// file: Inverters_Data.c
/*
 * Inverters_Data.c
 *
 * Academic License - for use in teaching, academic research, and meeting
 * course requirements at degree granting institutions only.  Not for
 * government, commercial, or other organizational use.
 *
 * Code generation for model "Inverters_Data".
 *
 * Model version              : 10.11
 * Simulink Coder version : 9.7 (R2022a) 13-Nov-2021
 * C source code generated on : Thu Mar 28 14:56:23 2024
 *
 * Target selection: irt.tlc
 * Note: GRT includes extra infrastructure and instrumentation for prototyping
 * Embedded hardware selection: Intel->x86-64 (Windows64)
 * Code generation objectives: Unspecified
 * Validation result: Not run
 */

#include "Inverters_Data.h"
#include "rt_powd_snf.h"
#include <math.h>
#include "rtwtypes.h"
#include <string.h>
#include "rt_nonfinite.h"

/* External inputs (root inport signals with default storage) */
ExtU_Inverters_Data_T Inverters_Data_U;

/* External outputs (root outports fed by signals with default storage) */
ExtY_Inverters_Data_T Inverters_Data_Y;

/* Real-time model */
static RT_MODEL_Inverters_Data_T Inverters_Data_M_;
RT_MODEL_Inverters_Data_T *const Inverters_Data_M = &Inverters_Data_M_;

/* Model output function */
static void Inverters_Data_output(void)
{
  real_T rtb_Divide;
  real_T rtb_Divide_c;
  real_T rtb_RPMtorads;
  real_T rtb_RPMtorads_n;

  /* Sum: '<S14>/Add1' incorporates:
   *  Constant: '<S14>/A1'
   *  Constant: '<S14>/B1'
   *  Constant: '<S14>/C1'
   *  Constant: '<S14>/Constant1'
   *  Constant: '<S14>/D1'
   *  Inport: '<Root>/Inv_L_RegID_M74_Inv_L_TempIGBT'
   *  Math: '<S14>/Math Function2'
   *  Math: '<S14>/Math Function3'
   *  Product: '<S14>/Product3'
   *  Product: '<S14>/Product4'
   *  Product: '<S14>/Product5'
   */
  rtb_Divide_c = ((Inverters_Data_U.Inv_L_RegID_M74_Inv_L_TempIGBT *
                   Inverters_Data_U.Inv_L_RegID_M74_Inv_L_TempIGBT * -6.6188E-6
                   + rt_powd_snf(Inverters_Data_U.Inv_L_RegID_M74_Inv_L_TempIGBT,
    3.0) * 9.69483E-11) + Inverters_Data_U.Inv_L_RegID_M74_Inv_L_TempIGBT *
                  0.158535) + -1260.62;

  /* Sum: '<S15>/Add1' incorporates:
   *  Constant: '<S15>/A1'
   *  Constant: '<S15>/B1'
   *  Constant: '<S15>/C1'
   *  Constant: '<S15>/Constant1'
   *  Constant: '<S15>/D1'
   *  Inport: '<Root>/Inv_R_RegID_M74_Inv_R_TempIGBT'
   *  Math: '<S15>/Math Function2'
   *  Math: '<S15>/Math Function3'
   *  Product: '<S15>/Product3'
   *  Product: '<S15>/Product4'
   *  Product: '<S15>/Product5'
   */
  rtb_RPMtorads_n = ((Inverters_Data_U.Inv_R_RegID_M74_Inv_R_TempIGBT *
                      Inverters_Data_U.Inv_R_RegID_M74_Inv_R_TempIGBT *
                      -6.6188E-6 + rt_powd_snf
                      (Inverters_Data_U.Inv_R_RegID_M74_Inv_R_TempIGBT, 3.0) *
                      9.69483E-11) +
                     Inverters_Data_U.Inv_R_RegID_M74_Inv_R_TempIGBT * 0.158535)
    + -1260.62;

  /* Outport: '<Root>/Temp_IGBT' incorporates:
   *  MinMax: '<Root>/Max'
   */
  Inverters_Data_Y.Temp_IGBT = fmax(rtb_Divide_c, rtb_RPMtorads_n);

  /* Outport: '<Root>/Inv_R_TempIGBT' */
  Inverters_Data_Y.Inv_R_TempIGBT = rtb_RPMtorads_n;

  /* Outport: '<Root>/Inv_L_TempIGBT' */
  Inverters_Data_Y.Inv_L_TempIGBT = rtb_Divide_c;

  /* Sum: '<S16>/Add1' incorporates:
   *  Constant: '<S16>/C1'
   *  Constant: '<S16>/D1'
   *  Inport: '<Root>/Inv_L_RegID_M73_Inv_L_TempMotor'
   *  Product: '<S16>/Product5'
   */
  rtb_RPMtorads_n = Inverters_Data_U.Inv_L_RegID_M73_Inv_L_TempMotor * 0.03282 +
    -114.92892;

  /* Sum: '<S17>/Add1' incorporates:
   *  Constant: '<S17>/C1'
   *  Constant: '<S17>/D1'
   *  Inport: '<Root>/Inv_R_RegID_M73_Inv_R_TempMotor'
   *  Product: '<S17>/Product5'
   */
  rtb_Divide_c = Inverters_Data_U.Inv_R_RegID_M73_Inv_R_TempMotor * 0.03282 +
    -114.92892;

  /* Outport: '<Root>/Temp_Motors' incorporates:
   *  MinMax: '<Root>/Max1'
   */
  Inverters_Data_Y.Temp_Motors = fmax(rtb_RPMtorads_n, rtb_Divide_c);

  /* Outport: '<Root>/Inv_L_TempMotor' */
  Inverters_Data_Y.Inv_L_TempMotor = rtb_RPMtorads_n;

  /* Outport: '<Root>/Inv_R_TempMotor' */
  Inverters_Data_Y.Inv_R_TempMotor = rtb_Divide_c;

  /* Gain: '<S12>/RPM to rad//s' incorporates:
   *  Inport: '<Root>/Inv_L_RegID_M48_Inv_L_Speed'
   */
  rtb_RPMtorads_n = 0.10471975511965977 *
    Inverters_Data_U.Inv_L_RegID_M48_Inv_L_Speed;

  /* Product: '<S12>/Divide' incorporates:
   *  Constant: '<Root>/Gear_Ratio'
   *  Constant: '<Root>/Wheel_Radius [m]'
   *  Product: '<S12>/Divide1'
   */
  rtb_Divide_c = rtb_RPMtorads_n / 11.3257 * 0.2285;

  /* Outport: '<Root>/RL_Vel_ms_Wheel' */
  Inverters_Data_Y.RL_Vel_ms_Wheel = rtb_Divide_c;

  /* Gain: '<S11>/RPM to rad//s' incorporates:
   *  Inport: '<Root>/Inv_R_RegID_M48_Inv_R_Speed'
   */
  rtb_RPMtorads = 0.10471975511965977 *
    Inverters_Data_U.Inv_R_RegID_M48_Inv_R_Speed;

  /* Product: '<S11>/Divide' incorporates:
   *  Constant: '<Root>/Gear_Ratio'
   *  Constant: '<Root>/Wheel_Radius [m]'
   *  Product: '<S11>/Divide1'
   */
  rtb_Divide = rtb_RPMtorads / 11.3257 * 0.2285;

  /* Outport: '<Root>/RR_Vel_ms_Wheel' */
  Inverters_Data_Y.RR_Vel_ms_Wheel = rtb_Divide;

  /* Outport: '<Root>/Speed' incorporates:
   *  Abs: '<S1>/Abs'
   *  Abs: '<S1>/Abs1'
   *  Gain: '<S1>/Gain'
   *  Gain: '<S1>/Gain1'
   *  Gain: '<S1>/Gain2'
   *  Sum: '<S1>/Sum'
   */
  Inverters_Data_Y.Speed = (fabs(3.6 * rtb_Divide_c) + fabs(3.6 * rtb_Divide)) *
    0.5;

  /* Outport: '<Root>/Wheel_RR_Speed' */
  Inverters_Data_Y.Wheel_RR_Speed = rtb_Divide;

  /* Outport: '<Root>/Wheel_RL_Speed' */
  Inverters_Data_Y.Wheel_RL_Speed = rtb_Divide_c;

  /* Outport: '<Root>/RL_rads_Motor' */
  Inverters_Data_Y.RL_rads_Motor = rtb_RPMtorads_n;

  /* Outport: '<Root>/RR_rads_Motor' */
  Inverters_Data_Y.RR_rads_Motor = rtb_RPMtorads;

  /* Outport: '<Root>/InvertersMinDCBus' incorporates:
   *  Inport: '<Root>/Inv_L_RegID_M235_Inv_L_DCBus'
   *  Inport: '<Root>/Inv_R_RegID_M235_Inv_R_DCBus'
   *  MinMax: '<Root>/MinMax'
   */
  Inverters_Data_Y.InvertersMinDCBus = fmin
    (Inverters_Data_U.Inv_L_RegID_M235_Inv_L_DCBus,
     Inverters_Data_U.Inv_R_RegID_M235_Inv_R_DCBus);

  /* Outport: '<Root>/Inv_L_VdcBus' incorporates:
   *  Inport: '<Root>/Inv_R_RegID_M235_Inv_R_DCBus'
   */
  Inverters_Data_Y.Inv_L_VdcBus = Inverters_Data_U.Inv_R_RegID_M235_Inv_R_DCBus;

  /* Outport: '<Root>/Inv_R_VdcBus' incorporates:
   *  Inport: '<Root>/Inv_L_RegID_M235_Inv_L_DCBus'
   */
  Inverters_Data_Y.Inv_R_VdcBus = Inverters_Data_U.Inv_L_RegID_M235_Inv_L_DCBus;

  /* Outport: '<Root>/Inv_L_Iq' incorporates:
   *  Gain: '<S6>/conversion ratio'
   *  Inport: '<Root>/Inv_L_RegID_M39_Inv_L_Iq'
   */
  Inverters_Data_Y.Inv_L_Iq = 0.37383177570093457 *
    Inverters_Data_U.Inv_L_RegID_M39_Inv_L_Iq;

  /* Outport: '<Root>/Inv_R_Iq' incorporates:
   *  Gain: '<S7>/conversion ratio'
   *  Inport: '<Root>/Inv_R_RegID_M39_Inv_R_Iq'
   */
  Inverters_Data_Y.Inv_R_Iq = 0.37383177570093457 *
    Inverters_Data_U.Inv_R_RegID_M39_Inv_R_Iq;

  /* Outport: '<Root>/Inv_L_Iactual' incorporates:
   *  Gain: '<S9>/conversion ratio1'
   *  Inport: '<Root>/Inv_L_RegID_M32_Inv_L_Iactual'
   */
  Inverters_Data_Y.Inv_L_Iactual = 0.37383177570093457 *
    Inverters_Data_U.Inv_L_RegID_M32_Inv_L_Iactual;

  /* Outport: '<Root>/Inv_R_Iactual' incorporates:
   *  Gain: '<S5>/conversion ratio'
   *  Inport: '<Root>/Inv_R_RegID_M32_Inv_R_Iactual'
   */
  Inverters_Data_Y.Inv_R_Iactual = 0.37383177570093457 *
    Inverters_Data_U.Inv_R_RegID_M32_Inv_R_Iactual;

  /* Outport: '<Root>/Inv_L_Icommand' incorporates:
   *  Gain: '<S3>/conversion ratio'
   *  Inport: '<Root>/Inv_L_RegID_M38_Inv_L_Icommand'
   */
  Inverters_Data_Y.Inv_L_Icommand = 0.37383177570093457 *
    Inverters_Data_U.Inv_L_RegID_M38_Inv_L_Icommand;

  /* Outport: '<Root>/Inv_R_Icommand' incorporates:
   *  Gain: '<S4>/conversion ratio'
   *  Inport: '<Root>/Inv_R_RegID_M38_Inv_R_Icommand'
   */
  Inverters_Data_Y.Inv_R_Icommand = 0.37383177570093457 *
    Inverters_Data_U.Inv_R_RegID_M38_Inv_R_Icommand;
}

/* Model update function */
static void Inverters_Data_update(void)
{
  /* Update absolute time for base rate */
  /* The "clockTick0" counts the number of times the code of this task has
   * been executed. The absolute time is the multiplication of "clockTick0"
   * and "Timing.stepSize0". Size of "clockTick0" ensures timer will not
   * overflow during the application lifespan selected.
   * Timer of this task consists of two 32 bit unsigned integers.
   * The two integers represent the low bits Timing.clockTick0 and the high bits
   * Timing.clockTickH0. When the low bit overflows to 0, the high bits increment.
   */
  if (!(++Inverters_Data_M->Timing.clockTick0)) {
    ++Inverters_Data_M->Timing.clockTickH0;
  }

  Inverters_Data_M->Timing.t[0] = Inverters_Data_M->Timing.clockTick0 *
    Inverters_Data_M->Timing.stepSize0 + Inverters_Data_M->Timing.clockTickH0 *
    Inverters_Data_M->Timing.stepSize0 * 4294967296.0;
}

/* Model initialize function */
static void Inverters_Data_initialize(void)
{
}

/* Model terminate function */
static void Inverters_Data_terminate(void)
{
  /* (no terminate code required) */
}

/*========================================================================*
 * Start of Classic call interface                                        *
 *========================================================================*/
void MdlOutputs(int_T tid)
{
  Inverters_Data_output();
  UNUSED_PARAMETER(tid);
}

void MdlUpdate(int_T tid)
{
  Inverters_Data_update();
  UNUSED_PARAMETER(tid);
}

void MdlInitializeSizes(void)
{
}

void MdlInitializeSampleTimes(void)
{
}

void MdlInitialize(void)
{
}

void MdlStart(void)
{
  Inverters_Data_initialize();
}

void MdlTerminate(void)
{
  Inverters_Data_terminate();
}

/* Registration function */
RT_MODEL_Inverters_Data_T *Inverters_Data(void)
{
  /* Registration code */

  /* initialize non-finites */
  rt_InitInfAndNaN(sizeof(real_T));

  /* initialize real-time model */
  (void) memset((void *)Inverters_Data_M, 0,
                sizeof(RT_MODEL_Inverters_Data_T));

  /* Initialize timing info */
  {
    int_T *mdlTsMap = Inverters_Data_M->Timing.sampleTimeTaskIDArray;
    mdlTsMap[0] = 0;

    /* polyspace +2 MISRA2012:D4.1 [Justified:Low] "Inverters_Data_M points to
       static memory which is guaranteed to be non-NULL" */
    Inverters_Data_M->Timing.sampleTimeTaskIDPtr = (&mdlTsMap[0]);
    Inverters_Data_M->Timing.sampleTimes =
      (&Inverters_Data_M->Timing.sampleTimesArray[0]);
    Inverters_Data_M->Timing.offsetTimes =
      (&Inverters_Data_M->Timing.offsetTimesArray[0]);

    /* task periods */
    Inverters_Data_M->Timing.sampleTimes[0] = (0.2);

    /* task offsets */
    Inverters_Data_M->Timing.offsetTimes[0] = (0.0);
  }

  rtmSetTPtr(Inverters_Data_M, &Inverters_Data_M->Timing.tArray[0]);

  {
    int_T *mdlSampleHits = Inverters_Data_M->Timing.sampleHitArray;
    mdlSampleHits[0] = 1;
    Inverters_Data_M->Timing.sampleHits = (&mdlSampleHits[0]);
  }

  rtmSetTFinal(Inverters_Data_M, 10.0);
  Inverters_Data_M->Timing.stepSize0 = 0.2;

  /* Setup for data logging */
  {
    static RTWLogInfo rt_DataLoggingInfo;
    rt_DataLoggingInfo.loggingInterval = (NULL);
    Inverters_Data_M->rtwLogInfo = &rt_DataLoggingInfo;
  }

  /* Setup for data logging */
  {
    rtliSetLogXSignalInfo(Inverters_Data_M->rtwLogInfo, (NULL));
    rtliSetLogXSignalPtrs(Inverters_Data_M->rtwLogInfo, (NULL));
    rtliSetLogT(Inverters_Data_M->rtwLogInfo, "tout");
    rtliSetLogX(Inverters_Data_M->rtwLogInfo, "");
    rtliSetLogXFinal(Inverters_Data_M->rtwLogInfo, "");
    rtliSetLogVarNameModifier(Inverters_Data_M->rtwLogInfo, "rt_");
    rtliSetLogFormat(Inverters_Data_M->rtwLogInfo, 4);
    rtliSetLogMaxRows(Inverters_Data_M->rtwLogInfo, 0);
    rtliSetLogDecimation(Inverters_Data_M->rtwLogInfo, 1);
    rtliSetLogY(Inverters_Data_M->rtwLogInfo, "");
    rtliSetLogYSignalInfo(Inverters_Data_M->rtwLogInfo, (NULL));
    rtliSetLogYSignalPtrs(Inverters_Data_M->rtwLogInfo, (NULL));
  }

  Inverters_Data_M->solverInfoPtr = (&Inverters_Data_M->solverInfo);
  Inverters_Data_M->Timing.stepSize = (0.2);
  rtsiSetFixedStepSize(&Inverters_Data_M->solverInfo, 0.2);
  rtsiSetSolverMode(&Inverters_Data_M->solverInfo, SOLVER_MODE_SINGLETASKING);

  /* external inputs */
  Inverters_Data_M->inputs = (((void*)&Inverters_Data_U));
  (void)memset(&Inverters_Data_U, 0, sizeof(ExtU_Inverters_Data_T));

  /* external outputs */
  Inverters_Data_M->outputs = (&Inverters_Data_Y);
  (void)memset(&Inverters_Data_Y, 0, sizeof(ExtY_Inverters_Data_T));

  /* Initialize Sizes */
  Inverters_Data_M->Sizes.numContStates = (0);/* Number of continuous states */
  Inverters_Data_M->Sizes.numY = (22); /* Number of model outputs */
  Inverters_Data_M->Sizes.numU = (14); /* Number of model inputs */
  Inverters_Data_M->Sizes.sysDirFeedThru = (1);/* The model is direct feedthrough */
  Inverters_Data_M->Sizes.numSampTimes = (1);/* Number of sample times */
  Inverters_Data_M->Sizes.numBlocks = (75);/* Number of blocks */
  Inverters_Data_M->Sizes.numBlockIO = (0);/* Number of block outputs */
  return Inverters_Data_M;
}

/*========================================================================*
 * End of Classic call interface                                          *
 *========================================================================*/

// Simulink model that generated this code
simulink model "Inverters_Data"  (R2022a)
settings: Solver=FixedStepAuto  StartTime=0.0  StopTime=10.0  RelTol=1e-3

== system Inverters_Data ==
  note: Car Constants
  note: 0x26
      | InverterL I cmd Bits
  note: Bits -> raw value
  note: 0x27
      | InverterL Iq actual Bits
  note: 0x49
      |  InverterL T-motor Bits
  note: [nothing] -> physical value
  note: 0x4A
      | InverterL T-igbt Bits
  note: 0x20
      | InverterL I actual Bits
  note: 0xEB
      | InverterL Vdc-Bus Bits
  note: 0x30
      | InverterL N actual Bits
  note: Inverters
  Inv_L_RegID_M48_Inv_L_Speed : Inport
  Inv_L_RegID_M73_Inv_L_TempMotor : Inport  Port=2
  Inv_L_RegID_M74_Inv_L_TempIGBT : Inport  Port=3
  Inv_L_RegID_M235_Inv_L_DCBus : Inport  Port=4
  Inv_R_RegID_M32_Inv_R_Iactual : Inport  Port=5
  Inv_R_RegID_M38_Inv_R_Icommand : Inport  Port=6
  Inv_R_RegID_M39_Inv_R_Iq : Inport  Port=7
  Inv_L_RegID_M32_Inv_L_Iactual : Inport  Port=8
  Inv_L_RegID_M38_Inv_L_Icommand : Inport  Port=9
  Inv_R_RegID_M48_Inv_R_Speed : Inport  Port=10
  Inv_L_RegID_M39_Inv_L_Iq : Inport  Port=11
  Inv_R_RegID_M73_Inv_R_TempMotor : Inport  Port=12
  Inv_R_RegID_M74_Inv_R_TempIGBT : Inport  Port=13
  Inv_R_RegID_M235_Inv_R_DCBus : Inport  Port=14
  Average : Subsystem
  Gear_Ratio : Constant  Value=11.3257
  IL : Subsystem
  IL 1 : Subsystem
  IL 2 : Subsystem
  IL 3 : Subsystem
  IL 4 : Subsystem
  IL 5 : Subsystem
  IL1 : Subsystem
  IL2 : Subsystem
  Max : MinMax  Function=max  Inputs=2
  Max1 : MinMax  Function=max  Inputs=2
  MinMax : MinMax  Inputs=2
  Subsystem : Subsystem
  Subsystem1 : Subsystem
  Subsystem2 : Subsystem
  Subsystem3 : Subsystem
  Subsystem4 : Subsystem
  Subsystem5 : Subsystem
  Subsystem6 : Subsystem
  Subsystem7 : Subsystem
  Wheel_Radius [m] : Constant  Value=0.2285
  Temp_IGBT : Outport  VectorParamsAs1DForOutWhenUnconnected=off
  Temp_Motors : Outport  Port=2  VectorParamsAs1DForOutWhenUnconnected=off
  RL_Vel_ms_Wheel : Outport  Port=3  VectorParamsAs1DForOutWhenUnconnected=off
  RR_Vel_ms_Wheel : Outport  Port=4  VectorParamsAs1DForOutWhenUnconnected=off
  InvertersMinDCBus : Outport  Port=5  VectorParamsAs1DForOutWhenUnconnected=off
  Speed : Outport  Port=6  VectorParamsAs1DForOutWhenUnconnected=off
  Inv_L_Iq : Outport  Port=7  VectorParamsAs1DForOutWhenUnconnected=off
  Inv_R_Iq : Outport  Port=8  VectorParamsAs1DForOutWhenUnconnected=off
  Inv_L_Iactual : Outport  Port=9  VectorParamsAs1DForOutWhenUnconnected=off
  Inv_R_Iactual : Outport  Port=10  VectorParamsAs1DForOutWhenUnconnected=off
  Inv_L_Icommand : Outport  Port=11  VectorParamsAs1DForOutWhenUnconnected=off
  Inv_R_Icommand : Outport  Port=12  VectorParamsAs1DForOutWhenUnconnected=off
  Wheel_RR_Speed : Outport  Port=13  VectorParamsAs1DForOutWhenUnconnected=off
  Wheel_RL_Speed : Outport  Port=14  VectorParamsAs1DForOutWhenUnconnected=off
  Inv_L_TempMotor : Outport  Port=15  VectorParamsAs1DForOutWhenUnconnected=off
  Inv_R_TempMotor : Outport  Port=16  VectorParamsAs1DForOutWhenUnconnected=off
  Inv_R_TempIGBT : Outport  Port=17  VectorParamsAs1DForOutWhenUnconnected=off
  Inv_L_TempIGBT : Outport  Port=18  VectorParamsAs1DForOutWhenUnconnected=off
  Inv_L_VdcBus : Outport  Port=19  VectorParamsAs1DForOutWhenUnconnected=off
  Inv_R_VdcBus : Outport  Port=20  VectorParamsAs1DForOutWhenUnconnected=off
  RL_rads_Motor : Outport  Port=21  VectorParamsAs1DForOutWhenUnconnected=off
  RR_rads_Motor : Outport  Port=22  VectorParamsAs1DForOutWhenUnconnected=off
  wires:
  Max1/1 -> Temp_Motors/1
  Inv_R_RegID_M48_Inv_R_Speed/1 -> IL/1("N actual Bits ")
  Inv_R_RegID_M39_Inv_R_Iq/1 -> IL 5/1("Iq Bits ")
  [RR_ms] -> Average/2(m/s Wheel RR), Wheel_RR_Speed/1
  Inv_L_RegID_M39_Inv_L_Iq/1 -> IL 4/1("Iq Bits ")
  Subsystem6/1(" T-motor") -> Max1/1, Inv_L_TempMotor/1
  Subsystem2/2(m/s Wheel) -> [RL_ms], RL_Vel_ms_Wheel/1
  Subsystem4/1(T-igbt) -> Max/1, Inv_L_TempIGBT/1
  Subsystem1/2(m/s Wheel) -> [RR_ms], RR_Vel_ms_Wheel/1
  Inv_L_RegID_M74_Inv_L_TempIGBT/1 -> Subsystem4/1(T-igbt Bits)
  [RL_ms] -> Average/1(m/s Wheel RL), Wheel_RL_Speed/1
  Inv_R_RegID_M73_Inv_R_TempMotor/1 -> Subsystem7/1(" T-motor Bits")
  Average/1(Speed km/h) -> Speed/1
  Subsystem7/1(" T-motor") -> Max1/2, Inv_R_TempMotor/1
  MinMax/1 -> InvertersMinDCBus/1
  Inv_L_RegID_M32_Inv_L_Iactual/1 -> IL2/1("I actual Bits ")
  Inv_R_RegID_M38_Inv_R_Icommand/1 -> IL 2/1("I cmd Bits ")
  Inv_R_RegID_M74_Inv_R_TempIGBT/1 -> Subsystem5/1(T-igbt Bits)
  Max/1 -> Temp_IGBT/1
  Inv_L_RegID_M73_Inv_L_TempMotor/1 -> Subsystem6/1(" T-motor Bits")
  Inv_R_RegID_M32_Inv_R_Iactual/1 -> IL 3/1("I actual Bits ")
  Inv_L_RegID_M38_Inv_L_Icommand/1 -> IL 1/1("I cmd Bits ")
  IL 4/1(Iq) -> Inv_L_Iq/1
  IL 5/1(Iq) -> Inv_R_Iq/1
  IL 3/1(Iact) -> Inv_R_Iactual/1
  IL2/1(Iact) -> Inv_L_Iactual/1
  Subsystem5/1(T-igbt) -> Max/2, Inv_R_TempIGBT/1
  Inv_L_RegID_M235_Inv_L_DCBus/1 -> Subsystem/1(VdcBus Bits)
  Inv_R_RegID_M235_Inv_R_DCBus/1 -> Subsystem3/1(VdcBus Bits)
  Subsystem/1(VdcBus) -> MinMax/1, Inv_R_VdcBus/1
  Subsystem3/1(VdcBus) -> Inv_L_VdcBus/1, MinMax/2
  IL 2/1(I cmd) -> Inv_R_Icommand/1
  IL 1/1(I cmd) -> Inv_L_Icommand/1
  Subsystem1/1(rad/s Motor) -> RR_rads_Motor/1
  Subsystem2/1(rad/s Motor) -> RL_rads_Motor/1
  Wheel_Radius [m]/1 -> [Wheel_Radius]
  Gear_Ratio/1 -> [Gear_Ratio]
  IL/1(RPM) -> Subsystem1/1(RPM Motor)
  [Gear_Ratio] -> Subsystem2/3(Gear_Ratio)
  [Wheel_Radius] -> Subsystem2/2(Wheel_Radius [m])
  IL1/1(RPM) -> Subsystem2/1(RPM Motor)
  [Gear_Ratio] -> Subsystem1/3(Gear_Ratio)
  [Wheel_Radius] -> Subsystem1/2(Wheel_Radius [m])
  Inv_L_RegID_M48_Inv_L_Speed/1 -> IL1/1("N actual Bits ")

== system Inverters_Data/Average ==
  m/s Wheel RL : Inport
  m/s Wheel RR : Inport  Port=2
  Abs : Abs  SaturateOnIntegerOverflow=off
  Abs1 : Abs  SaturateOnIntegerOverflow=off
  Gain : Gain  Gain=1/2
  Gain1 : Gain  Gain=3.6
  Gain2 : Gain  Gain=3.6
  Sum : Sum
  Speed km/h : Outport  VectorParamsAs1DForOutWhenUnconnected=off
  wires:
  m/s Wheel RR/1 -> Gain2/1
  Gain/1 -> Speed km/h/1
  Sum/1 -> Gain/1
  m/s Wheel RL/1 -> Gain1/1
  Abs1/1 -> Sum/1
  Abs/1 -> Sum/2
  Gain1/1 -> Abs1/1
  Gain2/1 -> Abs/1

== system Inverters_Data/IL ==
  note: Conversión hecha en Database
  note: 5000/32767=0.152593
  "N actual Bits " : Inport
  direction : Gain
  RPM : Outport  VectorParamsAs1DForOutWhenUnconnected=off
  wires:
  "N actual Bits "/1 -> direction/1
  direction/1 -> RPM/1

== system Inverters_Data/IL 1 ==
  "I cmd Bits " : Inport
  conversion ratio : Gain  Gain=400/1070
  I cmd : Outport  VectorParamsAs1DForOutWhenUnconnected=off
  wires:
  "I cmd Bits "/1 -> conversion ratio/1
  conversion ratio/1 -> I cmd/1

== system Inverters_Data/IL 2 ==
  "I cmd Bits " : Inport
  conversion ratio : Gain  Gain=400/1070
  I cmd : Outport  VectorParamsAs1DForOutWhenUnconnected=off
  wires:
  "I cmd Bits "/1 -> conversion ratio/1
  conversion ratio/1 -> I cmd/1

== system Inverters_Data/IL 3 ==
  "I actual Bits " : Inport
  conversion ratio : Gain  Gain=400/1070
  Iact : Outport  VectorParamsAs1DForOutWhenUnconnected=off
  wires:
  "I actual Bits "/1 -> conversion ratio/1
  conversion ratio/1 -> Iact/1

== system Inverters_Data/IL 4 ==
  "Iq Bits " : Inport
  conversion ratio : Gain  Gain=400/1070
  Iq : Outport  VectorParamsAs1DForOutWhenUnconnected=off
  wires:
  "Iq Bits "/1 -> conversion ratio/1
  conversion ratio/1 -> Iq/1

== system Inverters_Data/IL 5 ==
  "Iq Bits " : Inport
  conversion ratio : Gain  Gain=400/1070
  Iq : Outport  VectorParamsAs1DForOutWhenUnconnected=off
  wires:
  "Iq Bits "/1 -> conversion ratio/1
  conversion ratio/1 -> Iq/1

== system Inverters_Data/IL1 ==
  note: 5000/32767=0.152593
  note: Conversión hecha en Database
  "N actual Bits " : Inport
  direction : Gain
  RPM : Outport  VectorParamsAs1DForOutWhenUnconnected=off
  wires:
  direction/1 -> RPM/1
  "N actual Bits "/1 -> direction/1

== system Inverters_Data/IL2 ==
  "I actual Bits " : Inport
  conversion ratio1 : Gain  Gain=400/1070
  Iact : Outport  VectorParamsAs1DForOutWhenUnconnected=off
  wires:
  "I actual Bits "/1 -> conversion ratio1/1
  conversion ratio1/1 -> Iact/1

== system Inverters_Data/Subsystem ==
  note: Conversión hecha en database: "Inv_L_DCBus" (experimental)
  VdcBus Bits : Inport
  Gain : Gain
  VdcBus : Outport  VectorParamsAs1DForOutWhenUnconnected=off
  wires:
  VdcBus Bits/1 -> Gain/1
  Gain/1 -> VdcBus/1

== system Inverters_Data/Subsystem1 ==
  note: rad/s Wheel
  note: GR=n_Mot/n_Wheel=Tq_Wheel/Tq_Mot
  RPM Motor : Inport
  Wheel_Radius [m] : Inport  Port=2
  Gear_Ratio : Inport  Port=3
  Divide : Product  Inputs=**
  Divide1 : Product  Inputs=*/
  RPM to rad/s : Gain  Gain=2*pi/60
  rad/s Motor : Outport  VectorParamsAs1DForOutWhenUnconnected=off
  m/s Wheel : Outport  Port=2
  wires:
  RPM Motor/1 -> RPM to rad/s/1
  RPM to rad/s/1 -> Divide1/1, rad/s Motor/1
  Divide1/1 -> Divide/1
  Wheel_Radius [m]/1 -> Divide/2
  Divide/1 -> m/s Wheel/1
  Gear_Ratio/1 -> Divide1/2

== system Inverters_Data/Subsystem2 ==
  note: rad/s Wheel
  note: GR=n_Mot/n_Wheel=Tq_Wheel/Tq_Mot
  RPM Motor : Inport
  Wheel_Radius [m] : Inport  Port=2
  Gear_Ratio : Inport  Port=3
  Divide : Product  Inputs=**
  Divide1 : Product  Inputs=*/
  RPM to rad/s : Gain  Gain=2*pi/60
  rad/s Motor : Outport  VectorParamsAs1DForOutWhenUnconnected=off
  m/s Wheel : Outport  Port=2
  wires:
  RPM Motor/1 -> RPM to rad/s/1
  RPM to rad/s/1 -> Divide1/1, rad/s Motor/1
  Divide1/1 -> Divide/1
  Wheel_Radius [m]/1 -> Divide/2
  Divide/1 -> m/s Wheel/1
  Gear_Ratio/1 -> Divide1/2

== system Inverters_Data/Subsystem3 ==
  note: Conversión hecha en database: "Inv_R_DCBus" (experimental)
  VdcBus Bits : Inport
  Gain : Gain
  VdcBus : Outport  VectorParamsAs1DForOutWhenUnconnected=off
  wires:
  VdcBus Bits/1 -> Gain/1
  Gain/1 -> VdcBus/1

== system Inverters_Data/Subsystem4 ==
  T-igbt Bits : Inport
  A1 : Constant  Value=9.69483e-11
  Add1 : Sum  Inputs=++++
  B1 : Constant  Value=-6.6188e-6
  C1 : Constant  Value=0.158535
  Constant1 : Constant  Value=3
  D1 : Constant  Value=-1260.62
  Math Function2 : Math  Operator=pow  SignedPower=on
  Math Function3 : Math  Operator=square  SignedPower=on
  Product3 : Product
  Product4 : Product
  Product5 : Product
  T-igbt : Outport  VectorParamsAs1DForOutWhenUnconnected=off
  wires:
  Constant1/1 -> Math Function2/2
  Math Function3/1 -> Product4/1
  A1/1 -> Product3/2
  B1/1 -> Product4/2
  C1/1 -> Product5/2
  Product3/1 -> Add1/1
  Math Function2/1 -> Product3/1
  T-igbt Bits/1 -> Product5/1, Math Function3/1, Math Function2/1
  D1/1 -> Add1/4
  Add1/1 -> T-igbt/1
  Product5/1 -> Add1/3
  Product4/1 -> Add1/2

== system Inverters_Data/Subsystem5 ==
  T-igbt Bits : Inport
  A1 : Constant  Value=9.69483e-11
  Add1 : Sum  Inputs=++++
  B1 : Constant  Value=-6.6188e-6
  C1 : Constant  Value=0.158535
  Constant1 : Constant  Value=3
  D1 : Constant  Value=-1260.62
  Math Function2 : Math  Operator=pow  SignedPower=on
  Math Function3 : Math  Operator=square  SignedPower=on
  Product3 : Product
  Product4 : Product
  Product5 : Product
  T-igbt : Outport  VectorParamsAs1DForOutWhenUnconnected=off
  wires:
  Constant1/1 -> Math Function2/2
  Math Function3/1 -> Product4/1
  A1/1 -> Product3/2
  B1/1 -> Product4/2
  C1/1 -> Product5/2
  Product3/1 -> Add1/1
  Math Function2/1 -> Product3/1
  T-igbt Bits/1 -> Product5/1, Math Function3/1, Math Function2/1
  D1/1 -> Add1/4
  Add1/1 -> T-igbt/1
  Product5/1 -> Add1/3
  Product4/1 -> Add1/2

== system Inverters_Data/Subsystem6 ==
  " T-motor Bits" : Inport
  Add1 : Sum
  C1 : Constant  Value=0.03282
  D1 : Constant  Value=-114.92892
  Product5 : Product
  " T-motor" : Outport  VectorParamsAs1DForOutWhenUnconnected=off
  wires:
  Product5/1 -> Add1/1
  D1/1 -> Add1/2
  C1/1 -> Product5/2
  Add1/1 -> " T-motor"/1
  " T-motor Bits"/1 -> Product5/1

== system Inverters_Data/Subsystem7 ==
  " T-motor Bits" : Inport
  Add1 : Sum
  C1 : Constant  Value=0.03282
  D1 : Constant  Value=-114.92892
  Product5 : Product
  " T-motor" : Outport  VectorParamsAs1DForOutWhenUnconnected=off
  wires:
  Product5/1 -> Add1/1
  D1/1 -> Add1/2
  C1/1 -> Product5/2
  Add1/1 -> " T-motor"/1
  " T-motor Bits"/1 -> Product5/1
